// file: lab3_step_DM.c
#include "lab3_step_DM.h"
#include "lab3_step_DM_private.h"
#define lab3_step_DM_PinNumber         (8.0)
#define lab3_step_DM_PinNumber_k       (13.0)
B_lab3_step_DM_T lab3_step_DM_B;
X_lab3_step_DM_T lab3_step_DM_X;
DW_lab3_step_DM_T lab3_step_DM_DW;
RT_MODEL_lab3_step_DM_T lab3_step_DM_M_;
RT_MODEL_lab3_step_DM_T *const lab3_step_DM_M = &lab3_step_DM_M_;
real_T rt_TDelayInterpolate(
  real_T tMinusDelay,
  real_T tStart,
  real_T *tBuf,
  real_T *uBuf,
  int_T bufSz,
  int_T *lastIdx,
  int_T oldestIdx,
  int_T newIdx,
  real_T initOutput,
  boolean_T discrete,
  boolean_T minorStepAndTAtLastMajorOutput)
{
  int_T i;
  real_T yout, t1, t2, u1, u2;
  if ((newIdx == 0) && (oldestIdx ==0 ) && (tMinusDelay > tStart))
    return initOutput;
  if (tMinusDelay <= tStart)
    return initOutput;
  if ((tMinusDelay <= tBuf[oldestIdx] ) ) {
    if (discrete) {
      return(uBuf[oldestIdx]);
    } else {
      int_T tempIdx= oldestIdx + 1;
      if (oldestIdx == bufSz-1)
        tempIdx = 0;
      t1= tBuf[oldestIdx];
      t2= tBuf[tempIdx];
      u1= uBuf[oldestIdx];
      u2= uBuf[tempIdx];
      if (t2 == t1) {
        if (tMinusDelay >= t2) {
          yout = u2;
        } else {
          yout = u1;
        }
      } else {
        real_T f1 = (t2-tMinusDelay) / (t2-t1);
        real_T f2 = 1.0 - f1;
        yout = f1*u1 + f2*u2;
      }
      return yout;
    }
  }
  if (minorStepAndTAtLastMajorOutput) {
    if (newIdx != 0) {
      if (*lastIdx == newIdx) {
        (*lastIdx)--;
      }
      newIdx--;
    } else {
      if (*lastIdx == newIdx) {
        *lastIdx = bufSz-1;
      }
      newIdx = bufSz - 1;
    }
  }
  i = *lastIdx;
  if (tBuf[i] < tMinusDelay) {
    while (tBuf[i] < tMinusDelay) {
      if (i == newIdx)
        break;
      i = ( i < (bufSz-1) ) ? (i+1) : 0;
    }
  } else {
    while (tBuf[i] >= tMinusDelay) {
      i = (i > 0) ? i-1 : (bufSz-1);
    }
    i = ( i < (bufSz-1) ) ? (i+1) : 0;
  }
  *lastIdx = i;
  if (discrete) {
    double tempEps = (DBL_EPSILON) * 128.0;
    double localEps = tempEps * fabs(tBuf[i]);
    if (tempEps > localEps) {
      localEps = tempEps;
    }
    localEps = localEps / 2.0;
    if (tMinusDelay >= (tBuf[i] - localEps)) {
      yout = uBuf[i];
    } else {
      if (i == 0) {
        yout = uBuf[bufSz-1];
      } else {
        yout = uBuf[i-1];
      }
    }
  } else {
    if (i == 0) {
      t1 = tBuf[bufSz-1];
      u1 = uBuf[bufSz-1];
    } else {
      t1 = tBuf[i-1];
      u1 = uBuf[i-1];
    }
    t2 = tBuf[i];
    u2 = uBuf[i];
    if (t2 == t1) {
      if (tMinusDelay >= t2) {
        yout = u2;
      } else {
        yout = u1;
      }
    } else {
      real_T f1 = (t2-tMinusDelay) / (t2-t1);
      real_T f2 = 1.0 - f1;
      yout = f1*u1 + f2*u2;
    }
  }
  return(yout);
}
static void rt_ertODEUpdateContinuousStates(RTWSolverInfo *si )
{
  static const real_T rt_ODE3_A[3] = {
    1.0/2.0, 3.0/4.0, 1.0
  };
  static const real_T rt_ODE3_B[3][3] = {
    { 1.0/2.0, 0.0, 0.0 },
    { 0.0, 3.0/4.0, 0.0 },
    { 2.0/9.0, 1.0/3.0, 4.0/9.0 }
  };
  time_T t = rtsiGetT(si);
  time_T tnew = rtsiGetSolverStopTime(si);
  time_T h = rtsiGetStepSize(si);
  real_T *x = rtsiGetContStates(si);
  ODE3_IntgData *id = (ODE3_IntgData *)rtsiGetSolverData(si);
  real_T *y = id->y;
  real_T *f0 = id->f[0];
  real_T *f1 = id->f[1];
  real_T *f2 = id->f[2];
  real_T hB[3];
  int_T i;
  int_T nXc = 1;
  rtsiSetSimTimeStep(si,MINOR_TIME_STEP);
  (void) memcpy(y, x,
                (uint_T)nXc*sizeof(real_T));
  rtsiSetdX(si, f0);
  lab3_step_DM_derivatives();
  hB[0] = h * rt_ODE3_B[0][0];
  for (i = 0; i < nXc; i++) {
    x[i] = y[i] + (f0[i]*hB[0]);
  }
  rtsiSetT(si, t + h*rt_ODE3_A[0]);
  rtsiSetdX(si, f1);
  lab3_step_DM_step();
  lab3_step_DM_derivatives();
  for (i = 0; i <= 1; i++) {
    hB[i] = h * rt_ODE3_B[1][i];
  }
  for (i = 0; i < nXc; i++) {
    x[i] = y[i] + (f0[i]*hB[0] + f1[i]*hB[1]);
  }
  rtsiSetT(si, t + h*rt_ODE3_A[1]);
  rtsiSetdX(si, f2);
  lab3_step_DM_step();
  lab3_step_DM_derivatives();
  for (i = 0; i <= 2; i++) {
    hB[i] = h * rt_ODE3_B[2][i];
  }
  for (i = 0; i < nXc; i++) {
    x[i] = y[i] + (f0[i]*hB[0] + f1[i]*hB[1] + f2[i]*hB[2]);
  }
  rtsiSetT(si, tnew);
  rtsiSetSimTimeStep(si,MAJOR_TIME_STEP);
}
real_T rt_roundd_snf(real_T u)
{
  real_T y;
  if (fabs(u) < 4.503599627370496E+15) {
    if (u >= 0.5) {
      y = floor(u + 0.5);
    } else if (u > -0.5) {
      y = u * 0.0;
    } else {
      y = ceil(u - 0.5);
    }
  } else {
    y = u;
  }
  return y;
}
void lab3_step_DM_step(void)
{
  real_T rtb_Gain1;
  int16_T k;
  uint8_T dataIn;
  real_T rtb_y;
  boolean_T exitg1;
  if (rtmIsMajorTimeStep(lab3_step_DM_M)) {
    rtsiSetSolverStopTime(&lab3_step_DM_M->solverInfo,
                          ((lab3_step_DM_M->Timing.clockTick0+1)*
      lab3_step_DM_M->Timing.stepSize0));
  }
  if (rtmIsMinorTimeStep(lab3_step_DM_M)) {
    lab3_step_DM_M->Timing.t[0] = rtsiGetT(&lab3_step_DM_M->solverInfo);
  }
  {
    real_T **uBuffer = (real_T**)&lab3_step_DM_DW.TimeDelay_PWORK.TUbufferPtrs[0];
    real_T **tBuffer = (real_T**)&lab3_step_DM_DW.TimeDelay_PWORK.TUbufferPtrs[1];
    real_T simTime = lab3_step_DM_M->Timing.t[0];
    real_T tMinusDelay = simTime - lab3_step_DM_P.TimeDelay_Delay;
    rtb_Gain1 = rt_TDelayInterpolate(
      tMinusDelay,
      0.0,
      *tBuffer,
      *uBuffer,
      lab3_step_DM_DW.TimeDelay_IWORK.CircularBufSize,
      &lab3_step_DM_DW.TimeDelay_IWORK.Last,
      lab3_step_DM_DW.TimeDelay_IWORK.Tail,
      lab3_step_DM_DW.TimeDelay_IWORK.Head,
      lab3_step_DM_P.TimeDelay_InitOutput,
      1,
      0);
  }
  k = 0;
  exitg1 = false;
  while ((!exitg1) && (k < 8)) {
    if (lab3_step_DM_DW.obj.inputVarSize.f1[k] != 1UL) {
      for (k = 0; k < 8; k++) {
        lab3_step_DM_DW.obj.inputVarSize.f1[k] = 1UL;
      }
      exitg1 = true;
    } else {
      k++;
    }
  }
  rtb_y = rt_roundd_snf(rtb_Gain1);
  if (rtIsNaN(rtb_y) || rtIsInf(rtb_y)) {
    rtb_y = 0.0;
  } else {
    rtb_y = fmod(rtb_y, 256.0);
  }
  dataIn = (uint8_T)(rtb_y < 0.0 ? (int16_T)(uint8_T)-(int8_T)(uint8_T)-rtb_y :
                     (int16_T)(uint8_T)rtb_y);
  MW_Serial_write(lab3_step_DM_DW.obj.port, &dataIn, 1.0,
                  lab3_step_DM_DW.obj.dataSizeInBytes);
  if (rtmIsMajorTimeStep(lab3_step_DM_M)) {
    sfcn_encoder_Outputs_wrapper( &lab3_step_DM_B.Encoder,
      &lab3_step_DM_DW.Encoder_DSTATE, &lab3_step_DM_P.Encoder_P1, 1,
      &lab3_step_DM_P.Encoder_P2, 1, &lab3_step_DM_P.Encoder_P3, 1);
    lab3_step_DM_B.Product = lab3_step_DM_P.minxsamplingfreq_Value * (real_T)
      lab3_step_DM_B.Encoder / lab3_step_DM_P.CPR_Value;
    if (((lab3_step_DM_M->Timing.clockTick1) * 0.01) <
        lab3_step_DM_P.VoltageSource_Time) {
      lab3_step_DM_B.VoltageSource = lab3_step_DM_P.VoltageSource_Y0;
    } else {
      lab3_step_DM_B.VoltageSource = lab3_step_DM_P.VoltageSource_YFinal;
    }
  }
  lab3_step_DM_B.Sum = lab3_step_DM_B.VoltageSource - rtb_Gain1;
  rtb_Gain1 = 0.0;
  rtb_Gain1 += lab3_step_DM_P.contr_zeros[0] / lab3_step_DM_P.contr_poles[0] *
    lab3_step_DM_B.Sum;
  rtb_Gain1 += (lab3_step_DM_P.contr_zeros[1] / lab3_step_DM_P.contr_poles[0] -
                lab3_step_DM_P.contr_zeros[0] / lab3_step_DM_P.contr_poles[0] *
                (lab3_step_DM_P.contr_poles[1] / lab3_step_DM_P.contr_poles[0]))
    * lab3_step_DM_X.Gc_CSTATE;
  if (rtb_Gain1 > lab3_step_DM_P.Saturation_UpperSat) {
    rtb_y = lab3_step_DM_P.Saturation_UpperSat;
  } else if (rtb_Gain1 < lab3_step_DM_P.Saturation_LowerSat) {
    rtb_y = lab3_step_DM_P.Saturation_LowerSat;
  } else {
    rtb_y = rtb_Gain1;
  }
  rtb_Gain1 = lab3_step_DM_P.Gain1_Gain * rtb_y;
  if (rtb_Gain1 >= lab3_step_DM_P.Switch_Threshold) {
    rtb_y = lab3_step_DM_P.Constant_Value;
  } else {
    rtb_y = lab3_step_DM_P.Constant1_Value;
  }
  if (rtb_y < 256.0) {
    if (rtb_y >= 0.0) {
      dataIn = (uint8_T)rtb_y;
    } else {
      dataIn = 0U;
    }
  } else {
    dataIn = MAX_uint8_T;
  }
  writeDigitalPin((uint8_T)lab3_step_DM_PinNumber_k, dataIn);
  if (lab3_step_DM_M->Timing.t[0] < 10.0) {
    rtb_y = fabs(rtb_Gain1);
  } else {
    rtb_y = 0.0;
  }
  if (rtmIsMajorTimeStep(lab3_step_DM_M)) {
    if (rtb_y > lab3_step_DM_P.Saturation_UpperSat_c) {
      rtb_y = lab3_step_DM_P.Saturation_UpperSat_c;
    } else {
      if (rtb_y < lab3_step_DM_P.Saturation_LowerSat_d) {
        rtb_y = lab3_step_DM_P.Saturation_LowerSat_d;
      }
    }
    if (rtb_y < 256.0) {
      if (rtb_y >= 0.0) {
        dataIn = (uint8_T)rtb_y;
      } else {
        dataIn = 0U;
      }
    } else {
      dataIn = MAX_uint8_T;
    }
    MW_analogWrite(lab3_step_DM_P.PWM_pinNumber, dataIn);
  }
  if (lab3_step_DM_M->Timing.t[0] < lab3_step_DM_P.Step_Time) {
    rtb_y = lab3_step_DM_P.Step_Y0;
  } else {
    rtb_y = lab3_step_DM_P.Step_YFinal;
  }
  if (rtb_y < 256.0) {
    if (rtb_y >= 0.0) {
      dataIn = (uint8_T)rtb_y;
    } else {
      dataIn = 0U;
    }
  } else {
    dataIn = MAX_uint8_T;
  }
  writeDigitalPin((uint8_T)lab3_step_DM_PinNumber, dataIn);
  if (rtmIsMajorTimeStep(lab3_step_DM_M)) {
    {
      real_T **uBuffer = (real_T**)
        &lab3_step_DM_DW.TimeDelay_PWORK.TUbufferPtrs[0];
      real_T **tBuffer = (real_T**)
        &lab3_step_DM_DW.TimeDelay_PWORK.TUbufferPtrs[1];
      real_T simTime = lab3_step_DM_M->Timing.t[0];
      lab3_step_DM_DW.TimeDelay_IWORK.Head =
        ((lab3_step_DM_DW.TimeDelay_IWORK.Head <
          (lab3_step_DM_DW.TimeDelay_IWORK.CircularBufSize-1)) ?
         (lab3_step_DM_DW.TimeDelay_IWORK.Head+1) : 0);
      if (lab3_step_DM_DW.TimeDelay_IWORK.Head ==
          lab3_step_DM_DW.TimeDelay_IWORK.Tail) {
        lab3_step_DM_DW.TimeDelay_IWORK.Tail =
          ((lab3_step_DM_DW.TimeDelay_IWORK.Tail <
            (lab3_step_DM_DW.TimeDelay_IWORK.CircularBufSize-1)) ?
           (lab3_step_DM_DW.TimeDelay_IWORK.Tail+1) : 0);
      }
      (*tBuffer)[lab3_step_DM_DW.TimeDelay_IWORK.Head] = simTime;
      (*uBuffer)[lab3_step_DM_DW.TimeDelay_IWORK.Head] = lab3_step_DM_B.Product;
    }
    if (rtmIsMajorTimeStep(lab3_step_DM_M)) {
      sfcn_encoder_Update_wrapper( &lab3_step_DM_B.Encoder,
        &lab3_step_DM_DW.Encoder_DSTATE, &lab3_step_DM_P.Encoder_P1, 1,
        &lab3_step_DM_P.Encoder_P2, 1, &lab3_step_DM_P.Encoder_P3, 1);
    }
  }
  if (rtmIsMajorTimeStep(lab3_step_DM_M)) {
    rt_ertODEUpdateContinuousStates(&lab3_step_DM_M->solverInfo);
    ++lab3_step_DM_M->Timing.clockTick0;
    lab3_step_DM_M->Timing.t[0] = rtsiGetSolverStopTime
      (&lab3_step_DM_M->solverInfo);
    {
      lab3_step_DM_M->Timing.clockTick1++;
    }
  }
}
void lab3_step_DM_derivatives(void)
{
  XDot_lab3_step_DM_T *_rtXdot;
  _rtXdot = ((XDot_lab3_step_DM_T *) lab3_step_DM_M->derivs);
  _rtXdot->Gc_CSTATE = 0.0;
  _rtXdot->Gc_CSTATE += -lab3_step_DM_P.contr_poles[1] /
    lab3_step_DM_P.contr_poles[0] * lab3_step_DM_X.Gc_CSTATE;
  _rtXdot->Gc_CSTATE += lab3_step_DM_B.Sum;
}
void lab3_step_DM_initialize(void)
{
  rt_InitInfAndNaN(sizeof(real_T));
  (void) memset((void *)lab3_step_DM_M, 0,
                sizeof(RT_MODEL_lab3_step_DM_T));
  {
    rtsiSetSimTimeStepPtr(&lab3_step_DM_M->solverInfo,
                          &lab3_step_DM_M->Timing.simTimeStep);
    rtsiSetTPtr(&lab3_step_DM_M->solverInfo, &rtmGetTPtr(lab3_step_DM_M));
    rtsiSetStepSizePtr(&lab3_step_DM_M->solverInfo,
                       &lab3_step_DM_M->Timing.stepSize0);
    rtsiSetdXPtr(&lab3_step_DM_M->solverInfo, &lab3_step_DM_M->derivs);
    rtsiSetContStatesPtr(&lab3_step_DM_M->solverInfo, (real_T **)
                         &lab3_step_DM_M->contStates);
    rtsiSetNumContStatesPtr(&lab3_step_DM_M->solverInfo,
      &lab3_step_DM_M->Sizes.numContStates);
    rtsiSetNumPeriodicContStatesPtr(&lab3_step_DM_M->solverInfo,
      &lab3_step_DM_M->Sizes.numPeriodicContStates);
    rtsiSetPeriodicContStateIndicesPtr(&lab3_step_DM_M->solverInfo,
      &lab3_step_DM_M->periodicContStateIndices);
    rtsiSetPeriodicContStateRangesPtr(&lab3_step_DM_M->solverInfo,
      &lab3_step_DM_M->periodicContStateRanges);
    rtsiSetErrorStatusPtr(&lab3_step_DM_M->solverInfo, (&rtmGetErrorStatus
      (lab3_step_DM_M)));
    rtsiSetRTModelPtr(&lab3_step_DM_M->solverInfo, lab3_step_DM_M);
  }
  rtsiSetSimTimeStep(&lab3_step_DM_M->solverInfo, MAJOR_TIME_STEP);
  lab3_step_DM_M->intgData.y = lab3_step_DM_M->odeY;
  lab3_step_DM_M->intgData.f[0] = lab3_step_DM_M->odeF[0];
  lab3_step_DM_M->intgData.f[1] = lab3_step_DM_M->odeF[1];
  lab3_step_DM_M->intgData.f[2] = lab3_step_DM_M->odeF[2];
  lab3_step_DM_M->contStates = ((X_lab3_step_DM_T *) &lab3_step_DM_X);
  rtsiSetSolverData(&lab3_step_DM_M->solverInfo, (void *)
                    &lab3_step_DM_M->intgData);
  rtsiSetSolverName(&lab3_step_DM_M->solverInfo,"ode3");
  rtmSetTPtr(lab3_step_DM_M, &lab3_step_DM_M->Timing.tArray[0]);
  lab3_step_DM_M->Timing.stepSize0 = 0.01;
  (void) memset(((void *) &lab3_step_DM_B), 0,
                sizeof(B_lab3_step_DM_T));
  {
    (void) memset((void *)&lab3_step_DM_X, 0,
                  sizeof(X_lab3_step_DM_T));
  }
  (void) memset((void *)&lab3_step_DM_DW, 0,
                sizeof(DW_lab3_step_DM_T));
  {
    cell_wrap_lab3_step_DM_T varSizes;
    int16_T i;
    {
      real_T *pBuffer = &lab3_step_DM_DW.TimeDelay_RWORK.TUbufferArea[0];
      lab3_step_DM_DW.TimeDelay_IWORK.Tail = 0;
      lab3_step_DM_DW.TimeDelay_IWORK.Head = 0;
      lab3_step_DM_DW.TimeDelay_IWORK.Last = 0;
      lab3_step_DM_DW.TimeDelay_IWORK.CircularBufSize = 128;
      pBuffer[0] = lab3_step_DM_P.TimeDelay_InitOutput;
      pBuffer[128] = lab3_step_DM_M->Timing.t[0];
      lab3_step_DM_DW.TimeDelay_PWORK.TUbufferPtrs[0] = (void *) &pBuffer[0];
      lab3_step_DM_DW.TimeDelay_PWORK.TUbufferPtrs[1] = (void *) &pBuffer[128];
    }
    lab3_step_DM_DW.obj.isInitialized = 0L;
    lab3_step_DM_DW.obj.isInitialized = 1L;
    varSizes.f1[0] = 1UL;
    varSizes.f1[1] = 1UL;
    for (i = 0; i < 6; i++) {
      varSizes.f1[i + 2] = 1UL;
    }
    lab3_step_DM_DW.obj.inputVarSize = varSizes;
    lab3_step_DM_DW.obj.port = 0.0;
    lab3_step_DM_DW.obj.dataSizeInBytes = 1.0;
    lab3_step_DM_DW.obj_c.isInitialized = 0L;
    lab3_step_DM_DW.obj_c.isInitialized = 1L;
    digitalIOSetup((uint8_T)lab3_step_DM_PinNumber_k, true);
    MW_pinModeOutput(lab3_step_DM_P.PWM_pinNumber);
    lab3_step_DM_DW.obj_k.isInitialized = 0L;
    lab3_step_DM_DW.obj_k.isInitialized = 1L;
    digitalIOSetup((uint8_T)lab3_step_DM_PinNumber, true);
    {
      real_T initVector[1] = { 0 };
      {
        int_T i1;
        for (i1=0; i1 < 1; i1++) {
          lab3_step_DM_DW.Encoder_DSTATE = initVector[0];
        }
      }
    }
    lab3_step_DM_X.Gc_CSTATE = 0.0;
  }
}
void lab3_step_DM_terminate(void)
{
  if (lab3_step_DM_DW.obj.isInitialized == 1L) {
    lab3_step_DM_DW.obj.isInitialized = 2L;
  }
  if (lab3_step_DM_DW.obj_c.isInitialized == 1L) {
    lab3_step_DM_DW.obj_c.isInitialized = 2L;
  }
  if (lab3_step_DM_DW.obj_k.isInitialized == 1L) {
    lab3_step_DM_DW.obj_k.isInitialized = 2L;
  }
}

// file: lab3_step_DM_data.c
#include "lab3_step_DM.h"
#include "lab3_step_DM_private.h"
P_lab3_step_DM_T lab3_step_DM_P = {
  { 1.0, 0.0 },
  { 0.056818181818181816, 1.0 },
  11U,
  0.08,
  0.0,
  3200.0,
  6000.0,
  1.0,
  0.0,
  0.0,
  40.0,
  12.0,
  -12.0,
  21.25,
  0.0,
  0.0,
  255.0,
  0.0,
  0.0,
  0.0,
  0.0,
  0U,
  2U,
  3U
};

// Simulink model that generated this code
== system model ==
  SerialTransmit#1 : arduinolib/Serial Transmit  <- 1: DataTypeConversion#1
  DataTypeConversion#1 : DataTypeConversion  <- 1: TimeDelay
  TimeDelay : TransportDelay  <- 1: Product
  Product : Product  Inputs=**/  <- 1: minxsamplingfreq, 2: DataTypeConversion#2, 3: CPR
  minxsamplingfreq : Constant  Value=6000
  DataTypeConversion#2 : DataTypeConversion  <- 1: Encoder
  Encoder : S-Function  FunctionName=sfcn_encoder
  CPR : Constant  Value=3200
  DigitalOutput#1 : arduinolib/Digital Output  pinNumber=13  <- 1: hardlim#1
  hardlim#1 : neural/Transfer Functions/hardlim  <- 1: Gain1
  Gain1 : Gain  Gain=255/12  <- 1: Saturation
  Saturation : Saturate  UpperLimit=12  LowerLimit=-12  <- 1: Gc
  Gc : TransferFcn  Numerator=contr_zeros  Denominator=contr_poles  <- 1: Sum
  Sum : Sum  Inputs=+-  <- 1: VoltageSource, 2: TimeDelay
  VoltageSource : Step  Time=0  After=40
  PWM : arduinolib/PWM  pinNumber=11  <- 1: Saturate#1
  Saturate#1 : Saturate  UpperLimit=255  LowerLimit=0  <- 1: MATLABFunction#1
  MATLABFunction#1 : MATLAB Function  <- 1: Abs#1, 2: Clock#1
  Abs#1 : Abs  <- 1: Gain1
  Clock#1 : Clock
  DigitalOutput#2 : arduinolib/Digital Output  pinNumber=8  <- 1: Step
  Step : Step  Time=0  After=0
== matlab function MATLABFunction#1 ==
function y = fcn(u,c)
%#codegen
if c<10
    y = u;
else
    y=0;
end
